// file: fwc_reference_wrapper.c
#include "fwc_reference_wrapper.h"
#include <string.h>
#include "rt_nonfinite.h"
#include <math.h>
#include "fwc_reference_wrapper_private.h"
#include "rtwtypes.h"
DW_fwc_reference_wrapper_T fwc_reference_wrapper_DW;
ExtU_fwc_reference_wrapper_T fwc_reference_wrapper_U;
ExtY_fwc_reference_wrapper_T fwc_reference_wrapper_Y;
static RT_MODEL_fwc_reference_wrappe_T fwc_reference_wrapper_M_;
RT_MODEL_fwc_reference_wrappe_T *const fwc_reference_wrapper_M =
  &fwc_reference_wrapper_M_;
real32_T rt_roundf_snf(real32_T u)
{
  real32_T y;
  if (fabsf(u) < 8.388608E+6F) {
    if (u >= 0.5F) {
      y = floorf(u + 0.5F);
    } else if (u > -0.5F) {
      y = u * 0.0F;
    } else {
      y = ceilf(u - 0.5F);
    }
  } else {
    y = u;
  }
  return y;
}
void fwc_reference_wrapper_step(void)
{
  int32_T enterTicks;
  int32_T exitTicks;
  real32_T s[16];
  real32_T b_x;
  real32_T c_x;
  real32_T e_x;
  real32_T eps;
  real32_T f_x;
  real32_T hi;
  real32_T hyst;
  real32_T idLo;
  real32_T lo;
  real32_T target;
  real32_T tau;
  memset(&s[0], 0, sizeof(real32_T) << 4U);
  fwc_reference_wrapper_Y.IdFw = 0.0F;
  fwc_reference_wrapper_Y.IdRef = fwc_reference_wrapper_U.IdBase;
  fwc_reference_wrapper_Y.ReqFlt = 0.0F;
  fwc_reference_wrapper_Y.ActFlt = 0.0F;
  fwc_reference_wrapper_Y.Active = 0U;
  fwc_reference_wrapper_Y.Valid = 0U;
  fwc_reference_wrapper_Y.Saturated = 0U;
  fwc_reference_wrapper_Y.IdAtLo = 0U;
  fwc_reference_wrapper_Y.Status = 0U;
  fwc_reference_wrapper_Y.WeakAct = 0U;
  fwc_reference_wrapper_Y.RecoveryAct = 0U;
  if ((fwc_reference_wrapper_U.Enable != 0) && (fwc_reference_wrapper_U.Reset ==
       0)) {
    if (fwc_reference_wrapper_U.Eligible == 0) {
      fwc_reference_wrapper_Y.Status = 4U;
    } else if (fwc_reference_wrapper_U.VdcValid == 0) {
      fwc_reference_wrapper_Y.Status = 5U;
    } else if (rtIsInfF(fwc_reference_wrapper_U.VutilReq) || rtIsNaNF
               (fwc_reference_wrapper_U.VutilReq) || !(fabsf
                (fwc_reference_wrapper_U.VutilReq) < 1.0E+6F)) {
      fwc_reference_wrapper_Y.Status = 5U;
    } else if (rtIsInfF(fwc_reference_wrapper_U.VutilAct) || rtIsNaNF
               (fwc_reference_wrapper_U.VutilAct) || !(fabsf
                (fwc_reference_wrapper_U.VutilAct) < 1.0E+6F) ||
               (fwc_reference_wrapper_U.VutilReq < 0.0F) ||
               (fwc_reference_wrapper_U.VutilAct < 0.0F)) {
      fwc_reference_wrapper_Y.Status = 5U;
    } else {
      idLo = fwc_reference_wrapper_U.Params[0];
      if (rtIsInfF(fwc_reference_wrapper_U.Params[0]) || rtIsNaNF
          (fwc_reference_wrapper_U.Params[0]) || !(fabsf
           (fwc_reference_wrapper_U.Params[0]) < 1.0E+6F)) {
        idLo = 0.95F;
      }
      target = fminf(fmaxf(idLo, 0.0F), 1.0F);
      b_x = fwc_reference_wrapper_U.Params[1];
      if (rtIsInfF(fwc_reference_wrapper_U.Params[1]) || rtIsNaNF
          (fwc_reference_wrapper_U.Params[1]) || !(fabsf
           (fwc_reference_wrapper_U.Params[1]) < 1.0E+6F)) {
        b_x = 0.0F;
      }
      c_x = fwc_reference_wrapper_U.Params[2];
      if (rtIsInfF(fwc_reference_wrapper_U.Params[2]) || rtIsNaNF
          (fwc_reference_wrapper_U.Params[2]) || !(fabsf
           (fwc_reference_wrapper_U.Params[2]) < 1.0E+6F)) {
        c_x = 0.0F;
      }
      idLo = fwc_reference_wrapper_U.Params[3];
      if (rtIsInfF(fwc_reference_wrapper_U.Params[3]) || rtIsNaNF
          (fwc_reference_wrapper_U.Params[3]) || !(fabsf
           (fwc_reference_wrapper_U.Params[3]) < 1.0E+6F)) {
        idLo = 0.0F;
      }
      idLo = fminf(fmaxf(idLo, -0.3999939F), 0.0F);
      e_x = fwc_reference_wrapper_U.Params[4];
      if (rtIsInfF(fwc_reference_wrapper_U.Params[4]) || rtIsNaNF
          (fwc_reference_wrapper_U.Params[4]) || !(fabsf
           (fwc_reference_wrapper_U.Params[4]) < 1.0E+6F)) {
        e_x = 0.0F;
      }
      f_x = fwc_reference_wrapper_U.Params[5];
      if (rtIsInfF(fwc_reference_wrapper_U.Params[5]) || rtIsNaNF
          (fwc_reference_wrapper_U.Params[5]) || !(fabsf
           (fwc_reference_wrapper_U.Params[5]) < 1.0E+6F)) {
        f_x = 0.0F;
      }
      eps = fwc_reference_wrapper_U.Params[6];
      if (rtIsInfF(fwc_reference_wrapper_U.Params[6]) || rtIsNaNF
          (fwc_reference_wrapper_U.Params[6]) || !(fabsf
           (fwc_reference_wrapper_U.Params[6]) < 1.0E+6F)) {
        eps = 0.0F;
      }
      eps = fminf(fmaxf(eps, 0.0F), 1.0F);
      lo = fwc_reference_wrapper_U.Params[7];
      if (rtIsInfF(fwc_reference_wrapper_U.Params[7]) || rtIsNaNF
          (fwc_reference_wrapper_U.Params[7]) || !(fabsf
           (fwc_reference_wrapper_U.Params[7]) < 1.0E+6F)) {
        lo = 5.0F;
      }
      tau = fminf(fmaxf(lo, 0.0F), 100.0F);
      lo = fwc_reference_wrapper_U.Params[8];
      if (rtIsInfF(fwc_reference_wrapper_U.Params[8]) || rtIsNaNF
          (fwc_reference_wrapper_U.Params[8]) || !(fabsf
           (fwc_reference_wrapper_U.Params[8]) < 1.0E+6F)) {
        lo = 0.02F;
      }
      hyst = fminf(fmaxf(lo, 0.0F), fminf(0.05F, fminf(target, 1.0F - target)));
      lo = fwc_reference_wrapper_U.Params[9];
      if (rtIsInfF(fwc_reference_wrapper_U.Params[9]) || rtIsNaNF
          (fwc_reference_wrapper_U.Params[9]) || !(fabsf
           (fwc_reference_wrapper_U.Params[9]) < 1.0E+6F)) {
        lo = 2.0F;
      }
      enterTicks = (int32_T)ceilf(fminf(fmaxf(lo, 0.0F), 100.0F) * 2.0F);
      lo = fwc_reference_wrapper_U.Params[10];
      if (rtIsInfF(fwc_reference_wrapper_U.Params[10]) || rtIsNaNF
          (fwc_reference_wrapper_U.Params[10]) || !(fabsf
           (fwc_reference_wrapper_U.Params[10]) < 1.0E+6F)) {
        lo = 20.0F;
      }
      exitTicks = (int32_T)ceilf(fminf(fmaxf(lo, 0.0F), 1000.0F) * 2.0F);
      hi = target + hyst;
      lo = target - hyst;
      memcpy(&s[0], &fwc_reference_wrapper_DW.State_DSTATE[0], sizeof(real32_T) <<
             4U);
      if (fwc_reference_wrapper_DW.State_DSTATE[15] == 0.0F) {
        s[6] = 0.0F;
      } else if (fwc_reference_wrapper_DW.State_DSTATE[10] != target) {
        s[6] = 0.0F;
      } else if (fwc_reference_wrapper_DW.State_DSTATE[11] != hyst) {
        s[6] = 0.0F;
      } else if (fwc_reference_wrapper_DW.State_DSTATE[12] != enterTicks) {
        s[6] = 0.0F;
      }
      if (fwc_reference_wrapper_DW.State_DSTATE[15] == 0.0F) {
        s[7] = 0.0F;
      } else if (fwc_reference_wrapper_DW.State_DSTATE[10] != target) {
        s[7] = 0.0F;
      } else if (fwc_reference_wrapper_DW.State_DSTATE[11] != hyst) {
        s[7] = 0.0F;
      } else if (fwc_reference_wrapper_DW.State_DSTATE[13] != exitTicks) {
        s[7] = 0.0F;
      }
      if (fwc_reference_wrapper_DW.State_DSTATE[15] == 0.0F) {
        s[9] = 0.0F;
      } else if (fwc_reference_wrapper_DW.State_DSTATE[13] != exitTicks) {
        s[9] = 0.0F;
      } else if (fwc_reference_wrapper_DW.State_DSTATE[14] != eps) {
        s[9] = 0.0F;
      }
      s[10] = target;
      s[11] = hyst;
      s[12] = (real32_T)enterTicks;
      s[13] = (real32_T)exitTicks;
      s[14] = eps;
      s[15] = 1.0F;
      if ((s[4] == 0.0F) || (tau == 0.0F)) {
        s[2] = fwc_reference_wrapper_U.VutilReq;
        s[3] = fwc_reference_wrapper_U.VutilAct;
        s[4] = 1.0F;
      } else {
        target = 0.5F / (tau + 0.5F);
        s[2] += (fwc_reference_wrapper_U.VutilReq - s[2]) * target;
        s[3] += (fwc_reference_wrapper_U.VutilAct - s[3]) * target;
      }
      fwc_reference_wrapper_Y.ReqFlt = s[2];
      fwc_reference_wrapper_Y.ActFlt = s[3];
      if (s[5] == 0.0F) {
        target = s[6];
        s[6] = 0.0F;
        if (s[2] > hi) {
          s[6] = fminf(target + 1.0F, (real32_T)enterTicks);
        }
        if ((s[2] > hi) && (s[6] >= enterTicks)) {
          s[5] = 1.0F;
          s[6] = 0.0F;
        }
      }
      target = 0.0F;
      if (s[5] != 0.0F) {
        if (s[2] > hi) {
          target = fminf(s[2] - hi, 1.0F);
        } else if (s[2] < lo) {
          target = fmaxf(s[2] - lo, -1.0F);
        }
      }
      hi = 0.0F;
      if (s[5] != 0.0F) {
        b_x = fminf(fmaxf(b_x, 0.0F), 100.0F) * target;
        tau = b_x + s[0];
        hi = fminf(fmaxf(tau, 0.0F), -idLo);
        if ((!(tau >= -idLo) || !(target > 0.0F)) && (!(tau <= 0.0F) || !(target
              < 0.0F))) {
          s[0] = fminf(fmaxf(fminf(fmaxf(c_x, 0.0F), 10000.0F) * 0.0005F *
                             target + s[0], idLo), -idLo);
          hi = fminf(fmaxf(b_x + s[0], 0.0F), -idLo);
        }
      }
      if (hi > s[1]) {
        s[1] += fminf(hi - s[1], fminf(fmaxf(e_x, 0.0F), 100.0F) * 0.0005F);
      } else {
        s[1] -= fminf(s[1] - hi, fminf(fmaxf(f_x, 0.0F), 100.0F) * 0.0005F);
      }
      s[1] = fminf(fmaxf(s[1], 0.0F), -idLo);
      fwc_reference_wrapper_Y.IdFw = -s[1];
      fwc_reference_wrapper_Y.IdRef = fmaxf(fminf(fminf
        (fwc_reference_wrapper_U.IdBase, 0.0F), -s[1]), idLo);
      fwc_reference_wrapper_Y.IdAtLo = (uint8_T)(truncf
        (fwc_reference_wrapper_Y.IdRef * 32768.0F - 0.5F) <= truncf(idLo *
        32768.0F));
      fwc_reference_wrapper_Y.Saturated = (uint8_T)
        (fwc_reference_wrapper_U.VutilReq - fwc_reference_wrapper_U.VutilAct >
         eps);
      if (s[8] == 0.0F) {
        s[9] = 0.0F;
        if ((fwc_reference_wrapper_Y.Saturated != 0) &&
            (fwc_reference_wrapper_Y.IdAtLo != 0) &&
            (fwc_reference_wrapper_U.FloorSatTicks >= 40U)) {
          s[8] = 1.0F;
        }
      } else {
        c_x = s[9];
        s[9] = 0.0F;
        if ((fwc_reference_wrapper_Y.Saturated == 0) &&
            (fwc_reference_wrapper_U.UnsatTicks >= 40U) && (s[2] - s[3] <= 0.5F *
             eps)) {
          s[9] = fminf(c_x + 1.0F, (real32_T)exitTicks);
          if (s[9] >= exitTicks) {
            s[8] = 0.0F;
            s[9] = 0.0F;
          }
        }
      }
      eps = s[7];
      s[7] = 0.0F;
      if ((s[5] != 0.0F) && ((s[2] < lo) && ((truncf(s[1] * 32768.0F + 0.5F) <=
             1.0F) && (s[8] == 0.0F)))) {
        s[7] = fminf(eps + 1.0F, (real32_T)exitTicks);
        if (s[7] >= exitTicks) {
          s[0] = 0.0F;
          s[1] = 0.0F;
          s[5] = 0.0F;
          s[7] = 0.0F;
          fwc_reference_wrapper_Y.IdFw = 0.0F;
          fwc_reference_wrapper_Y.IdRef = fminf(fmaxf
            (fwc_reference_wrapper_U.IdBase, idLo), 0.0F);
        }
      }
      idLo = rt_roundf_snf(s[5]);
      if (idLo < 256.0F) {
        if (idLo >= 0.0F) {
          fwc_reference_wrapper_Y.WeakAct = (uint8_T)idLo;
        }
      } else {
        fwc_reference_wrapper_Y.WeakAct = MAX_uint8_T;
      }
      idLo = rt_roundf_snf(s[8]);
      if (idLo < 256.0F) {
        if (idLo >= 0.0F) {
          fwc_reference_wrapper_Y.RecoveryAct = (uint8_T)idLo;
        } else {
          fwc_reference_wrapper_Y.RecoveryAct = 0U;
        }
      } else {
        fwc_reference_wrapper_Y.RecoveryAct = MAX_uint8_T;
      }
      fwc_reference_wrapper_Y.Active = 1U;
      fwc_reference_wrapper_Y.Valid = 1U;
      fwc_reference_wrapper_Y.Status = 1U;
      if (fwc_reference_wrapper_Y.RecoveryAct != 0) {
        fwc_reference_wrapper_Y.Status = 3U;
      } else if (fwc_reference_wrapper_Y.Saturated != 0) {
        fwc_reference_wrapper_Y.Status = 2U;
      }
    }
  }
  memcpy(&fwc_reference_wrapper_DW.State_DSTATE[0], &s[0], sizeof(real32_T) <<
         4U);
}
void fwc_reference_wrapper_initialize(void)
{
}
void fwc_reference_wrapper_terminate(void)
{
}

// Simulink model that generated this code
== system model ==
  Enable : Inport
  Reset : Inport
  Eligible : Inport
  VdcValid : Inport
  VutilReq : Inport
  VutilAct : Inport
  IdBase : Inport
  Params : Inport
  FloorSatTicks : Inport
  UnsatTicks : Inport
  IdFw : Outport  <- 1: MATLABFunction#1/2
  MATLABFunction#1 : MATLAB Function  <- 1: Enable, 2: Reset, 3: Eligible, 4: VdcValid, 5: VutilReq, 6: VutilAct, 7: IdBase, 8: Params, 9: State, 10: FloorSatTicks, 11: UnsatTicks
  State : UnitDelay  InitialCondition=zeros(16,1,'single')  <- 1: MATLABFunction#1
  IdRef : Outport  <- 1: MATLABFunction#1/3
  Active : Outport  <- 1: MATLABFunction#1/4
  Valid : Outport  <- 1: MATLABFunction#1/5
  Saturated : Outport  <- 1: MATLABFunction#1/6
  IdAtLo : Outport  <- 1: MATLABFunction#1/7
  Status : Outport  <- 1: MATLABFunction#1/8
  ReqFlt : Outport  <- 1: MATLABFunction#1/9
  ActFlt : Outport  <- 1: MATLABFunction#1/10
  WeakAct : Outport  <- 1: MATLABFunction#1/11
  RecoveryAct : Outport  <- 1: MATLABFunction#1/12
== matlab function MATLABFunction#1 ==
function [nextState,idFw,idRef,active,valid,saturated,idAtLo,status,reqFlt,actFlt,weakAct,recoveryAct] = fcn(enable,reset,eligible,vdcValid,vutilReq,vutilAct,idBase,params,state,floorSatTicks,unsatTicks)
%#codegen
[nextState,idFw,idRef,active,valid,saturated,idAtLo,status,reqFlt,actFlt,weakAct,recoveryAct] = fwc_reference_step(enable,reset,eligible,vdcValid,vutilReq,vutilAct,idBase,state,params,floorSatTicks,unsatTicks);
end
